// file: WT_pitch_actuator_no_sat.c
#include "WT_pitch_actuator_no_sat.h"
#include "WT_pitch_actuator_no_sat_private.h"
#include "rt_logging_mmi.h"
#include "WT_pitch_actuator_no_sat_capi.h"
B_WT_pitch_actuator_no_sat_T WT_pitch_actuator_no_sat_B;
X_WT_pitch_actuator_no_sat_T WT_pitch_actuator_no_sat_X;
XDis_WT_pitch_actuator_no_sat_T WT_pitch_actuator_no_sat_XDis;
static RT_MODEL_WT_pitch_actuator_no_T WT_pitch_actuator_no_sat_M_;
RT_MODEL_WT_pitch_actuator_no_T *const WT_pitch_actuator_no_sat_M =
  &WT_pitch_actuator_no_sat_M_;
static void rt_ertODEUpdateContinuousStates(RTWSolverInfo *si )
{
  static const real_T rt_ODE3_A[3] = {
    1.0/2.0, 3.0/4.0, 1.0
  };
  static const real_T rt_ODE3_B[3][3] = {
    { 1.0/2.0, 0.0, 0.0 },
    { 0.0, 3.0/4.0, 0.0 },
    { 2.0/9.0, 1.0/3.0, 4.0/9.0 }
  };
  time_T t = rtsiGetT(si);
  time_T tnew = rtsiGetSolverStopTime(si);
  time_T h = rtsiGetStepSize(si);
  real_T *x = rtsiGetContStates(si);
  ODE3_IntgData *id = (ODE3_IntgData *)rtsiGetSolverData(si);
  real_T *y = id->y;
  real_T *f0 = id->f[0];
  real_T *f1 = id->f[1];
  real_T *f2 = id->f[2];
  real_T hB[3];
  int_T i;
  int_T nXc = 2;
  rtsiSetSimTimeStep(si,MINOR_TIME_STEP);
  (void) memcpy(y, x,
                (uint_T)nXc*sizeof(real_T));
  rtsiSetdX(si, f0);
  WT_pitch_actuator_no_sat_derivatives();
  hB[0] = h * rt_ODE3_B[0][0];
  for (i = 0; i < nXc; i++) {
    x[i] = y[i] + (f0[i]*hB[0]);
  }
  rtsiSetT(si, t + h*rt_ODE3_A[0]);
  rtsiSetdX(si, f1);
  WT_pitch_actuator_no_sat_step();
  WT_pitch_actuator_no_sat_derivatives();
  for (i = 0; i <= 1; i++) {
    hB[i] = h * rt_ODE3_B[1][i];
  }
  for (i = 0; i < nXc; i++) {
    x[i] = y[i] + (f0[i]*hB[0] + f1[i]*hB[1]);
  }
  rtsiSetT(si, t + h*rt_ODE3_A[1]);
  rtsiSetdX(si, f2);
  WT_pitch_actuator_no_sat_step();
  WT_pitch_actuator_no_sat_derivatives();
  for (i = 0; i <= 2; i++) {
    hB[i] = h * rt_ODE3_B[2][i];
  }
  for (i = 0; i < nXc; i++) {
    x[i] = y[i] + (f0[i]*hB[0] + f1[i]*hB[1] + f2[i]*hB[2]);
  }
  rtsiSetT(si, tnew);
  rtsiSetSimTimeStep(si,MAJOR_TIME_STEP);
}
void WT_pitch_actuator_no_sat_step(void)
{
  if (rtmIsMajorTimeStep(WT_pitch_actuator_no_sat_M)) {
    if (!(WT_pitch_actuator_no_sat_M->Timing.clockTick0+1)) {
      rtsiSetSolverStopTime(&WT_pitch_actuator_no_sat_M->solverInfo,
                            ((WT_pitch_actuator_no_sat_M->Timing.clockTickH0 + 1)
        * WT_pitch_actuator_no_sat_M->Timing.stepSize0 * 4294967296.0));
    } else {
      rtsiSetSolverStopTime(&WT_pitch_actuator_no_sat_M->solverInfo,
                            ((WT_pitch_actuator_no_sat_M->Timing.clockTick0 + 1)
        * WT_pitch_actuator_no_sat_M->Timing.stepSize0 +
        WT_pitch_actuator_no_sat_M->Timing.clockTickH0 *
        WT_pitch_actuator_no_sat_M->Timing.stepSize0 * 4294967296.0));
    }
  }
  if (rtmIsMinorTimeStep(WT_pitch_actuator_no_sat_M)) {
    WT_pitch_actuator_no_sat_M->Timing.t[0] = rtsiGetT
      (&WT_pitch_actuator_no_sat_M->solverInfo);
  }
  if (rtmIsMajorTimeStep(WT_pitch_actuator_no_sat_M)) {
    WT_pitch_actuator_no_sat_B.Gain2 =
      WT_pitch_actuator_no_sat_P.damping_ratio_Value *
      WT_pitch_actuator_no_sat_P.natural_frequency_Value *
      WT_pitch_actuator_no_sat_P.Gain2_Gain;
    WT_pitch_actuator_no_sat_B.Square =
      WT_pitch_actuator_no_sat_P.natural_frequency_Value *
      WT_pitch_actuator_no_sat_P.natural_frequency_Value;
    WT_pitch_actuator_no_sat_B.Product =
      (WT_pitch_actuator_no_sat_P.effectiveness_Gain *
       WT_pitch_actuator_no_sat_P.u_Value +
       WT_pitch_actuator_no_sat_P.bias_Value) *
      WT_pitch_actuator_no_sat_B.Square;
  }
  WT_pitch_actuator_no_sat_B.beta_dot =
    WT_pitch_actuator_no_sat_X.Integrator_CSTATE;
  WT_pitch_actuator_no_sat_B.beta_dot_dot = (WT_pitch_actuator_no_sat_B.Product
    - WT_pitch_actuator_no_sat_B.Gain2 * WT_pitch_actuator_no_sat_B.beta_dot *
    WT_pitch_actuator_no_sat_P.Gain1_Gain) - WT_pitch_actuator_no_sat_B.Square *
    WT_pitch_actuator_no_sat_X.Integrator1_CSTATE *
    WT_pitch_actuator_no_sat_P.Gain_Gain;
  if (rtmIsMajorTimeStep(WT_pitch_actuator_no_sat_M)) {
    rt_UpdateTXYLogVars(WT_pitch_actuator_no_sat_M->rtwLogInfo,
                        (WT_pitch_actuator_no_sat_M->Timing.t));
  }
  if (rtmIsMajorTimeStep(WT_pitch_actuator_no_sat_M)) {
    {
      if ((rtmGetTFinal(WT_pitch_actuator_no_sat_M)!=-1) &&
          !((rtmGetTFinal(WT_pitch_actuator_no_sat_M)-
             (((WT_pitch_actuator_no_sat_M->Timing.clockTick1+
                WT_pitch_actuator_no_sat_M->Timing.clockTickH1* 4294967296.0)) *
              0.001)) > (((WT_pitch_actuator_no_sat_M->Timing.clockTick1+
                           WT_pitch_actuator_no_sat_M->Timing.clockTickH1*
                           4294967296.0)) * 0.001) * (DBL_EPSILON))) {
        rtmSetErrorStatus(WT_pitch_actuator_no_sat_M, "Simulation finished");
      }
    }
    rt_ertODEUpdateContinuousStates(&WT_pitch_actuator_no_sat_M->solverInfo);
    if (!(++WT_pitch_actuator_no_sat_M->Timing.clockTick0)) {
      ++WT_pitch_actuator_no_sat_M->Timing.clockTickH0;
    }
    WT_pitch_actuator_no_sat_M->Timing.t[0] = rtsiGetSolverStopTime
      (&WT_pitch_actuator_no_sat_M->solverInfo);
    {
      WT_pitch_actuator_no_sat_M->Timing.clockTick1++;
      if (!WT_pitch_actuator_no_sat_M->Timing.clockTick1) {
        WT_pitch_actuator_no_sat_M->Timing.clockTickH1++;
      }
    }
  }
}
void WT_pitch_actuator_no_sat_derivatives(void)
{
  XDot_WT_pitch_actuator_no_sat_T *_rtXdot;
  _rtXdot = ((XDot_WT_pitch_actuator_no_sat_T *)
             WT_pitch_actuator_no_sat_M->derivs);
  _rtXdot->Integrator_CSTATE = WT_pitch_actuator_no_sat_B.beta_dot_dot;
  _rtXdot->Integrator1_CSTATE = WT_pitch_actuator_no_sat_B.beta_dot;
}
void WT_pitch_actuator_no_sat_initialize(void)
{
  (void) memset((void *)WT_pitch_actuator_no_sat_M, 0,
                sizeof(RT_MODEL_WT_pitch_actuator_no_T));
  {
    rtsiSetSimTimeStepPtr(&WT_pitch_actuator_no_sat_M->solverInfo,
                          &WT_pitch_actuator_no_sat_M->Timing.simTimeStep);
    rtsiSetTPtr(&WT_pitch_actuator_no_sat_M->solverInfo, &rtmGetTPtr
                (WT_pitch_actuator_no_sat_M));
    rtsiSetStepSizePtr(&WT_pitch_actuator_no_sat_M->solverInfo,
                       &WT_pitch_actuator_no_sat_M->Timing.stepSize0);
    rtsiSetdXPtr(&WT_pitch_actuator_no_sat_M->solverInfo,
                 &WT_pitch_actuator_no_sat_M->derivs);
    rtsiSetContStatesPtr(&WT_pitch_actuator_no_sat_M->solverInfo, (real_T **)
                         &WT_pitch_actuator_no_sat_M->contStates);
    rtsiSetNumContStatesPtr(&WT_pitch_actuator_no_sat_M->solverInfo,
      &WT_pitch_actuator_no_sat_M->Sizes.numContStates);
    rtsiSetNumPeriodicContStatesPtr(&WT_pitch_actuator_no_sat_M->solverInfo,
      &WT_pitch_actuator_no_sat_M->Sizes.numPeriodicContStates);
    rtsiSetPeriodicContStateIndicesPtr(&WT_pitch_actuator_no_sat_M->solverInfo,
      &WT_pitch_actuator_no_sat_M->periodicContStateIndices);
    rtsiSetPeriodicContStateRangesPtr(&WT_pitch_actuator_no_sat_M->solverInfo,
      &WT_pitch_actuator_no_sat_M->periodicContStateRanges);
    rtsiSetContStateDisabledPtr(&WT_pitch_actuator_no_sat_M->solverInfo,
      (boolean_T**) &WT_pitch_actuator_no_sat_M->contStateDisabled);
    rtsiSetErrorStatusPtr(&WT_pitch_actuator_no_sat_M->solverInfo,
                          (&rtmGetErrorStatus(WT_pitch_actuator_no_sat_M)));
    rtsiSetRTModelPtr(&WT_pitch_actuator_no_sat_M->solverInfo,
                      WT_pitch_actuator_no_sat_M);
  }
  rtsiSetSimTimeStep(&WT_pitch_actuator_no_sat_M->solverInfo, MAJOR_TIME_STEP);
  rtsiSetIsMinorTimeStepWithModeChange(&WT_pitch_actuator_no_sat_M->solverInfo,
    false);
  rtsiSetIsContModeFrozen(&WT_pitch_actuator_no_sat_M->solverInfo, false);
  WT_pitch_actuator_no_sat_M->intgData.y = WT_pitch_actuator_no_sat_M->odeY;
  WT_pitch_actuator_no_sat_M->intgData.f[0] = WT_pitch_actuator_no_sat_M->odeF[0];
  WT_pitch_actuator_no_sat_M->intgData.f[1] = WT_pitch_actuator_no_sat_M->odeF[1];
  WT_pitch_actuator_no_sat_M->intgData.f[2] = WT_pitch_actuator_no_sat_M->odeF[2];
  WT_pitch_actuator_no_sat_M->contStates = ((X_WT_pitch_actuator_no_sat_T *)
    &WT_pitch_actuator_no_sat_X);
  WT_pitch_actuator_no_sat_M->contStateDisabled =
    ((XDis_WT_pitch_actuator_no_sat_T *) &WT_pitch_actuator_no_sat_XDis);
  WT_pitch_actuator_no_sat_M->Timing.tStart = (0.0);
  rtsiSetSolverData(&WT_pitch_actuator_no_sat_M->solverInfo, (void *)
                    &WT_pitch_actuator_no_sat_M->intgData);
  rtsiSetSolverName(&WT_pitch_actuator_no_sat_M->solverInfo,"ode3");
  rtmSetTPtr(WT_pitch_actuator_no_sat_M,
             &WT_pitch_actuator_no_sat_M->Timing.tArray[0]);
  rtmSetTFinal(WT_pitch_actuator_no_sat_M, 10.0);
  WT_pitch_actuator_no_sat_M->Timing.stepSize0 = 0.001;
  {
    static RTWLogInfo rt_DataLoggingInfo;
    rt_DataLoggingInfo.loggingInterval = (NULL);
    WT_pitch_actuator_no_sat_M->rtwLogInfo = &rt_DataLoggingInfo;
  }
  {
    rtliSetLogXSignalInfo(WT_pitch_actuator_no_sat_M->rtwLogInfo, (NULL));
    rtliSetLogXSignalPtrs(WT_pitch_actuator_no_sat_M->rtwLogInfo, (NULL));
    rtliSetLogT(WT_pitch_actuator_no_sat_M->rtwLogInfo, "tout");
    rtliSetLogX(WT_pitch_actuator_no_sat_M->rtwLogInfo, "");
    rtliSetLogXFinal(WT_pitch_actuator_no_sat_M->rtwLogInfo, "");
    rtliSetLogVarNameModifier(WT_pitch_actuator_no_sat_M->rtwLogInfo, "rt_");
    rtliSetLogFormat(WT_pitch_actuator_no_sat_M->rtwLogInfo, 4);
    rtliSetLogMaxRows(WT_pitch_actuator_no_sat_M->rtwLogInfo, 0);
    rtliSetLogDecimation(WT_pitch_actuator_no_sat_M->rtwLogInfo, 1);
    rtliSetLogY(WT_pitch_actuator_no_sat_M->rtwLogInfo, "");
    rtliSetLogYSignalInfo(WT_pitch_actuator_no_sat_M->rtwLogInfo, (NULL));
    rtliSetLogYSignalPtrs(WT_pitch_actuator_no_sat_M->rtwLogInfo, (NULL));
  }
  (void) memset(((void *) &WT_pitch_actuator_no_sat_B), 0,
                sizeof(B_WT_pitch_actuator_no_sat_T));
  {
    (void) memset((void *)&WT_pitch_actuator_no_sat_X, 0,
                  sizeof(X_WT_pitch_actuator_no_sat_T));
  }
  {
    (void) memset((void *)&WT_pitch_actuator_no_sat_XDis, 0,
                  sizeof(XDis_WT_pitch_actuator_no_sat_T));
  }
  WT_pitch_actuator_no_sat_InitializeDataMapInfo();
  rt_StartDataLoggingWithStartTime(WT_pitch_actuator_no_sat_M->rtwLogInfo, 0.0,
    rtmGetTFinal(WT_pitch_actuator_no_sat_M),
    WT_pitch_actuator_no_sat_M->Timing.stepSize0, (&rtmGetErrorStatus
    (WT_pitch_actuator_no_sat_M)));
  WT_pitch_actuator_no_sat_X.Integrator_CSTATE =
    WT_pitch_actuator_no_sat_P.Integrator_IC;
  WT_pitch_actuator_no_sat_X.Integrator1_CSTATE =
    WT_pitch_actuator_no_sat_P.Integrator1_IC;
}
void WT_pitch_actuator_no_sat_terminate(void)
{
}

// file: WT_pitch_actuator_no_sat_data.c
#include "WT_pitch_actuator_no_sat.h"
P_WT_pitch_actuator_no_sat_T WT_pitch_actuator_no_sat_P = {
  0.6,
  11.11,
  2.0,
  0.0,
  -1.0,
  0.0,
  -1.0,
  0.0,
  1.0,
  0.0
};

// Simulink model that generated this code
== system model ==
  Gain2 : Gain  Gain=2  <- 1: Product#1
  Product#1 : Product  <- 1: damping_ratio, 2: natural_frequency
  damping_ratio : Constant  Value=0.6
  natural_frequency : Constant  Value=11.11
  Square : Math  Operator=square  <- 1: natural_frequency
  Product : Product  <- 1: Square, 2: Sum#1
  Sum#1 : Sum  Inputs=++  <- 1: effectiveness, 2: bias
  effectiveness : Gain  <- 1: Constant#1
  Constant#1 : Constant  Value=0
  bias : Constant  Value=0
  Integrator : Integrator  <- 1: Sum#2
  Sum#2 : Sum  Inputs=--+  <- 1: Gain1, 2: Gain, 3: Product
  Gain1 : Gain  Gain=-1  <- 1: Product#2
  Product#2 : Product  <- 1: Gain2, 2: Integrator
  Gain : Gain  Gain=-1  <- 1: Product#3
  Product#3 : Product  <- 1: Square, 2: Integrator1
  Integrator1 : Integrator  <- 1: Integrator
